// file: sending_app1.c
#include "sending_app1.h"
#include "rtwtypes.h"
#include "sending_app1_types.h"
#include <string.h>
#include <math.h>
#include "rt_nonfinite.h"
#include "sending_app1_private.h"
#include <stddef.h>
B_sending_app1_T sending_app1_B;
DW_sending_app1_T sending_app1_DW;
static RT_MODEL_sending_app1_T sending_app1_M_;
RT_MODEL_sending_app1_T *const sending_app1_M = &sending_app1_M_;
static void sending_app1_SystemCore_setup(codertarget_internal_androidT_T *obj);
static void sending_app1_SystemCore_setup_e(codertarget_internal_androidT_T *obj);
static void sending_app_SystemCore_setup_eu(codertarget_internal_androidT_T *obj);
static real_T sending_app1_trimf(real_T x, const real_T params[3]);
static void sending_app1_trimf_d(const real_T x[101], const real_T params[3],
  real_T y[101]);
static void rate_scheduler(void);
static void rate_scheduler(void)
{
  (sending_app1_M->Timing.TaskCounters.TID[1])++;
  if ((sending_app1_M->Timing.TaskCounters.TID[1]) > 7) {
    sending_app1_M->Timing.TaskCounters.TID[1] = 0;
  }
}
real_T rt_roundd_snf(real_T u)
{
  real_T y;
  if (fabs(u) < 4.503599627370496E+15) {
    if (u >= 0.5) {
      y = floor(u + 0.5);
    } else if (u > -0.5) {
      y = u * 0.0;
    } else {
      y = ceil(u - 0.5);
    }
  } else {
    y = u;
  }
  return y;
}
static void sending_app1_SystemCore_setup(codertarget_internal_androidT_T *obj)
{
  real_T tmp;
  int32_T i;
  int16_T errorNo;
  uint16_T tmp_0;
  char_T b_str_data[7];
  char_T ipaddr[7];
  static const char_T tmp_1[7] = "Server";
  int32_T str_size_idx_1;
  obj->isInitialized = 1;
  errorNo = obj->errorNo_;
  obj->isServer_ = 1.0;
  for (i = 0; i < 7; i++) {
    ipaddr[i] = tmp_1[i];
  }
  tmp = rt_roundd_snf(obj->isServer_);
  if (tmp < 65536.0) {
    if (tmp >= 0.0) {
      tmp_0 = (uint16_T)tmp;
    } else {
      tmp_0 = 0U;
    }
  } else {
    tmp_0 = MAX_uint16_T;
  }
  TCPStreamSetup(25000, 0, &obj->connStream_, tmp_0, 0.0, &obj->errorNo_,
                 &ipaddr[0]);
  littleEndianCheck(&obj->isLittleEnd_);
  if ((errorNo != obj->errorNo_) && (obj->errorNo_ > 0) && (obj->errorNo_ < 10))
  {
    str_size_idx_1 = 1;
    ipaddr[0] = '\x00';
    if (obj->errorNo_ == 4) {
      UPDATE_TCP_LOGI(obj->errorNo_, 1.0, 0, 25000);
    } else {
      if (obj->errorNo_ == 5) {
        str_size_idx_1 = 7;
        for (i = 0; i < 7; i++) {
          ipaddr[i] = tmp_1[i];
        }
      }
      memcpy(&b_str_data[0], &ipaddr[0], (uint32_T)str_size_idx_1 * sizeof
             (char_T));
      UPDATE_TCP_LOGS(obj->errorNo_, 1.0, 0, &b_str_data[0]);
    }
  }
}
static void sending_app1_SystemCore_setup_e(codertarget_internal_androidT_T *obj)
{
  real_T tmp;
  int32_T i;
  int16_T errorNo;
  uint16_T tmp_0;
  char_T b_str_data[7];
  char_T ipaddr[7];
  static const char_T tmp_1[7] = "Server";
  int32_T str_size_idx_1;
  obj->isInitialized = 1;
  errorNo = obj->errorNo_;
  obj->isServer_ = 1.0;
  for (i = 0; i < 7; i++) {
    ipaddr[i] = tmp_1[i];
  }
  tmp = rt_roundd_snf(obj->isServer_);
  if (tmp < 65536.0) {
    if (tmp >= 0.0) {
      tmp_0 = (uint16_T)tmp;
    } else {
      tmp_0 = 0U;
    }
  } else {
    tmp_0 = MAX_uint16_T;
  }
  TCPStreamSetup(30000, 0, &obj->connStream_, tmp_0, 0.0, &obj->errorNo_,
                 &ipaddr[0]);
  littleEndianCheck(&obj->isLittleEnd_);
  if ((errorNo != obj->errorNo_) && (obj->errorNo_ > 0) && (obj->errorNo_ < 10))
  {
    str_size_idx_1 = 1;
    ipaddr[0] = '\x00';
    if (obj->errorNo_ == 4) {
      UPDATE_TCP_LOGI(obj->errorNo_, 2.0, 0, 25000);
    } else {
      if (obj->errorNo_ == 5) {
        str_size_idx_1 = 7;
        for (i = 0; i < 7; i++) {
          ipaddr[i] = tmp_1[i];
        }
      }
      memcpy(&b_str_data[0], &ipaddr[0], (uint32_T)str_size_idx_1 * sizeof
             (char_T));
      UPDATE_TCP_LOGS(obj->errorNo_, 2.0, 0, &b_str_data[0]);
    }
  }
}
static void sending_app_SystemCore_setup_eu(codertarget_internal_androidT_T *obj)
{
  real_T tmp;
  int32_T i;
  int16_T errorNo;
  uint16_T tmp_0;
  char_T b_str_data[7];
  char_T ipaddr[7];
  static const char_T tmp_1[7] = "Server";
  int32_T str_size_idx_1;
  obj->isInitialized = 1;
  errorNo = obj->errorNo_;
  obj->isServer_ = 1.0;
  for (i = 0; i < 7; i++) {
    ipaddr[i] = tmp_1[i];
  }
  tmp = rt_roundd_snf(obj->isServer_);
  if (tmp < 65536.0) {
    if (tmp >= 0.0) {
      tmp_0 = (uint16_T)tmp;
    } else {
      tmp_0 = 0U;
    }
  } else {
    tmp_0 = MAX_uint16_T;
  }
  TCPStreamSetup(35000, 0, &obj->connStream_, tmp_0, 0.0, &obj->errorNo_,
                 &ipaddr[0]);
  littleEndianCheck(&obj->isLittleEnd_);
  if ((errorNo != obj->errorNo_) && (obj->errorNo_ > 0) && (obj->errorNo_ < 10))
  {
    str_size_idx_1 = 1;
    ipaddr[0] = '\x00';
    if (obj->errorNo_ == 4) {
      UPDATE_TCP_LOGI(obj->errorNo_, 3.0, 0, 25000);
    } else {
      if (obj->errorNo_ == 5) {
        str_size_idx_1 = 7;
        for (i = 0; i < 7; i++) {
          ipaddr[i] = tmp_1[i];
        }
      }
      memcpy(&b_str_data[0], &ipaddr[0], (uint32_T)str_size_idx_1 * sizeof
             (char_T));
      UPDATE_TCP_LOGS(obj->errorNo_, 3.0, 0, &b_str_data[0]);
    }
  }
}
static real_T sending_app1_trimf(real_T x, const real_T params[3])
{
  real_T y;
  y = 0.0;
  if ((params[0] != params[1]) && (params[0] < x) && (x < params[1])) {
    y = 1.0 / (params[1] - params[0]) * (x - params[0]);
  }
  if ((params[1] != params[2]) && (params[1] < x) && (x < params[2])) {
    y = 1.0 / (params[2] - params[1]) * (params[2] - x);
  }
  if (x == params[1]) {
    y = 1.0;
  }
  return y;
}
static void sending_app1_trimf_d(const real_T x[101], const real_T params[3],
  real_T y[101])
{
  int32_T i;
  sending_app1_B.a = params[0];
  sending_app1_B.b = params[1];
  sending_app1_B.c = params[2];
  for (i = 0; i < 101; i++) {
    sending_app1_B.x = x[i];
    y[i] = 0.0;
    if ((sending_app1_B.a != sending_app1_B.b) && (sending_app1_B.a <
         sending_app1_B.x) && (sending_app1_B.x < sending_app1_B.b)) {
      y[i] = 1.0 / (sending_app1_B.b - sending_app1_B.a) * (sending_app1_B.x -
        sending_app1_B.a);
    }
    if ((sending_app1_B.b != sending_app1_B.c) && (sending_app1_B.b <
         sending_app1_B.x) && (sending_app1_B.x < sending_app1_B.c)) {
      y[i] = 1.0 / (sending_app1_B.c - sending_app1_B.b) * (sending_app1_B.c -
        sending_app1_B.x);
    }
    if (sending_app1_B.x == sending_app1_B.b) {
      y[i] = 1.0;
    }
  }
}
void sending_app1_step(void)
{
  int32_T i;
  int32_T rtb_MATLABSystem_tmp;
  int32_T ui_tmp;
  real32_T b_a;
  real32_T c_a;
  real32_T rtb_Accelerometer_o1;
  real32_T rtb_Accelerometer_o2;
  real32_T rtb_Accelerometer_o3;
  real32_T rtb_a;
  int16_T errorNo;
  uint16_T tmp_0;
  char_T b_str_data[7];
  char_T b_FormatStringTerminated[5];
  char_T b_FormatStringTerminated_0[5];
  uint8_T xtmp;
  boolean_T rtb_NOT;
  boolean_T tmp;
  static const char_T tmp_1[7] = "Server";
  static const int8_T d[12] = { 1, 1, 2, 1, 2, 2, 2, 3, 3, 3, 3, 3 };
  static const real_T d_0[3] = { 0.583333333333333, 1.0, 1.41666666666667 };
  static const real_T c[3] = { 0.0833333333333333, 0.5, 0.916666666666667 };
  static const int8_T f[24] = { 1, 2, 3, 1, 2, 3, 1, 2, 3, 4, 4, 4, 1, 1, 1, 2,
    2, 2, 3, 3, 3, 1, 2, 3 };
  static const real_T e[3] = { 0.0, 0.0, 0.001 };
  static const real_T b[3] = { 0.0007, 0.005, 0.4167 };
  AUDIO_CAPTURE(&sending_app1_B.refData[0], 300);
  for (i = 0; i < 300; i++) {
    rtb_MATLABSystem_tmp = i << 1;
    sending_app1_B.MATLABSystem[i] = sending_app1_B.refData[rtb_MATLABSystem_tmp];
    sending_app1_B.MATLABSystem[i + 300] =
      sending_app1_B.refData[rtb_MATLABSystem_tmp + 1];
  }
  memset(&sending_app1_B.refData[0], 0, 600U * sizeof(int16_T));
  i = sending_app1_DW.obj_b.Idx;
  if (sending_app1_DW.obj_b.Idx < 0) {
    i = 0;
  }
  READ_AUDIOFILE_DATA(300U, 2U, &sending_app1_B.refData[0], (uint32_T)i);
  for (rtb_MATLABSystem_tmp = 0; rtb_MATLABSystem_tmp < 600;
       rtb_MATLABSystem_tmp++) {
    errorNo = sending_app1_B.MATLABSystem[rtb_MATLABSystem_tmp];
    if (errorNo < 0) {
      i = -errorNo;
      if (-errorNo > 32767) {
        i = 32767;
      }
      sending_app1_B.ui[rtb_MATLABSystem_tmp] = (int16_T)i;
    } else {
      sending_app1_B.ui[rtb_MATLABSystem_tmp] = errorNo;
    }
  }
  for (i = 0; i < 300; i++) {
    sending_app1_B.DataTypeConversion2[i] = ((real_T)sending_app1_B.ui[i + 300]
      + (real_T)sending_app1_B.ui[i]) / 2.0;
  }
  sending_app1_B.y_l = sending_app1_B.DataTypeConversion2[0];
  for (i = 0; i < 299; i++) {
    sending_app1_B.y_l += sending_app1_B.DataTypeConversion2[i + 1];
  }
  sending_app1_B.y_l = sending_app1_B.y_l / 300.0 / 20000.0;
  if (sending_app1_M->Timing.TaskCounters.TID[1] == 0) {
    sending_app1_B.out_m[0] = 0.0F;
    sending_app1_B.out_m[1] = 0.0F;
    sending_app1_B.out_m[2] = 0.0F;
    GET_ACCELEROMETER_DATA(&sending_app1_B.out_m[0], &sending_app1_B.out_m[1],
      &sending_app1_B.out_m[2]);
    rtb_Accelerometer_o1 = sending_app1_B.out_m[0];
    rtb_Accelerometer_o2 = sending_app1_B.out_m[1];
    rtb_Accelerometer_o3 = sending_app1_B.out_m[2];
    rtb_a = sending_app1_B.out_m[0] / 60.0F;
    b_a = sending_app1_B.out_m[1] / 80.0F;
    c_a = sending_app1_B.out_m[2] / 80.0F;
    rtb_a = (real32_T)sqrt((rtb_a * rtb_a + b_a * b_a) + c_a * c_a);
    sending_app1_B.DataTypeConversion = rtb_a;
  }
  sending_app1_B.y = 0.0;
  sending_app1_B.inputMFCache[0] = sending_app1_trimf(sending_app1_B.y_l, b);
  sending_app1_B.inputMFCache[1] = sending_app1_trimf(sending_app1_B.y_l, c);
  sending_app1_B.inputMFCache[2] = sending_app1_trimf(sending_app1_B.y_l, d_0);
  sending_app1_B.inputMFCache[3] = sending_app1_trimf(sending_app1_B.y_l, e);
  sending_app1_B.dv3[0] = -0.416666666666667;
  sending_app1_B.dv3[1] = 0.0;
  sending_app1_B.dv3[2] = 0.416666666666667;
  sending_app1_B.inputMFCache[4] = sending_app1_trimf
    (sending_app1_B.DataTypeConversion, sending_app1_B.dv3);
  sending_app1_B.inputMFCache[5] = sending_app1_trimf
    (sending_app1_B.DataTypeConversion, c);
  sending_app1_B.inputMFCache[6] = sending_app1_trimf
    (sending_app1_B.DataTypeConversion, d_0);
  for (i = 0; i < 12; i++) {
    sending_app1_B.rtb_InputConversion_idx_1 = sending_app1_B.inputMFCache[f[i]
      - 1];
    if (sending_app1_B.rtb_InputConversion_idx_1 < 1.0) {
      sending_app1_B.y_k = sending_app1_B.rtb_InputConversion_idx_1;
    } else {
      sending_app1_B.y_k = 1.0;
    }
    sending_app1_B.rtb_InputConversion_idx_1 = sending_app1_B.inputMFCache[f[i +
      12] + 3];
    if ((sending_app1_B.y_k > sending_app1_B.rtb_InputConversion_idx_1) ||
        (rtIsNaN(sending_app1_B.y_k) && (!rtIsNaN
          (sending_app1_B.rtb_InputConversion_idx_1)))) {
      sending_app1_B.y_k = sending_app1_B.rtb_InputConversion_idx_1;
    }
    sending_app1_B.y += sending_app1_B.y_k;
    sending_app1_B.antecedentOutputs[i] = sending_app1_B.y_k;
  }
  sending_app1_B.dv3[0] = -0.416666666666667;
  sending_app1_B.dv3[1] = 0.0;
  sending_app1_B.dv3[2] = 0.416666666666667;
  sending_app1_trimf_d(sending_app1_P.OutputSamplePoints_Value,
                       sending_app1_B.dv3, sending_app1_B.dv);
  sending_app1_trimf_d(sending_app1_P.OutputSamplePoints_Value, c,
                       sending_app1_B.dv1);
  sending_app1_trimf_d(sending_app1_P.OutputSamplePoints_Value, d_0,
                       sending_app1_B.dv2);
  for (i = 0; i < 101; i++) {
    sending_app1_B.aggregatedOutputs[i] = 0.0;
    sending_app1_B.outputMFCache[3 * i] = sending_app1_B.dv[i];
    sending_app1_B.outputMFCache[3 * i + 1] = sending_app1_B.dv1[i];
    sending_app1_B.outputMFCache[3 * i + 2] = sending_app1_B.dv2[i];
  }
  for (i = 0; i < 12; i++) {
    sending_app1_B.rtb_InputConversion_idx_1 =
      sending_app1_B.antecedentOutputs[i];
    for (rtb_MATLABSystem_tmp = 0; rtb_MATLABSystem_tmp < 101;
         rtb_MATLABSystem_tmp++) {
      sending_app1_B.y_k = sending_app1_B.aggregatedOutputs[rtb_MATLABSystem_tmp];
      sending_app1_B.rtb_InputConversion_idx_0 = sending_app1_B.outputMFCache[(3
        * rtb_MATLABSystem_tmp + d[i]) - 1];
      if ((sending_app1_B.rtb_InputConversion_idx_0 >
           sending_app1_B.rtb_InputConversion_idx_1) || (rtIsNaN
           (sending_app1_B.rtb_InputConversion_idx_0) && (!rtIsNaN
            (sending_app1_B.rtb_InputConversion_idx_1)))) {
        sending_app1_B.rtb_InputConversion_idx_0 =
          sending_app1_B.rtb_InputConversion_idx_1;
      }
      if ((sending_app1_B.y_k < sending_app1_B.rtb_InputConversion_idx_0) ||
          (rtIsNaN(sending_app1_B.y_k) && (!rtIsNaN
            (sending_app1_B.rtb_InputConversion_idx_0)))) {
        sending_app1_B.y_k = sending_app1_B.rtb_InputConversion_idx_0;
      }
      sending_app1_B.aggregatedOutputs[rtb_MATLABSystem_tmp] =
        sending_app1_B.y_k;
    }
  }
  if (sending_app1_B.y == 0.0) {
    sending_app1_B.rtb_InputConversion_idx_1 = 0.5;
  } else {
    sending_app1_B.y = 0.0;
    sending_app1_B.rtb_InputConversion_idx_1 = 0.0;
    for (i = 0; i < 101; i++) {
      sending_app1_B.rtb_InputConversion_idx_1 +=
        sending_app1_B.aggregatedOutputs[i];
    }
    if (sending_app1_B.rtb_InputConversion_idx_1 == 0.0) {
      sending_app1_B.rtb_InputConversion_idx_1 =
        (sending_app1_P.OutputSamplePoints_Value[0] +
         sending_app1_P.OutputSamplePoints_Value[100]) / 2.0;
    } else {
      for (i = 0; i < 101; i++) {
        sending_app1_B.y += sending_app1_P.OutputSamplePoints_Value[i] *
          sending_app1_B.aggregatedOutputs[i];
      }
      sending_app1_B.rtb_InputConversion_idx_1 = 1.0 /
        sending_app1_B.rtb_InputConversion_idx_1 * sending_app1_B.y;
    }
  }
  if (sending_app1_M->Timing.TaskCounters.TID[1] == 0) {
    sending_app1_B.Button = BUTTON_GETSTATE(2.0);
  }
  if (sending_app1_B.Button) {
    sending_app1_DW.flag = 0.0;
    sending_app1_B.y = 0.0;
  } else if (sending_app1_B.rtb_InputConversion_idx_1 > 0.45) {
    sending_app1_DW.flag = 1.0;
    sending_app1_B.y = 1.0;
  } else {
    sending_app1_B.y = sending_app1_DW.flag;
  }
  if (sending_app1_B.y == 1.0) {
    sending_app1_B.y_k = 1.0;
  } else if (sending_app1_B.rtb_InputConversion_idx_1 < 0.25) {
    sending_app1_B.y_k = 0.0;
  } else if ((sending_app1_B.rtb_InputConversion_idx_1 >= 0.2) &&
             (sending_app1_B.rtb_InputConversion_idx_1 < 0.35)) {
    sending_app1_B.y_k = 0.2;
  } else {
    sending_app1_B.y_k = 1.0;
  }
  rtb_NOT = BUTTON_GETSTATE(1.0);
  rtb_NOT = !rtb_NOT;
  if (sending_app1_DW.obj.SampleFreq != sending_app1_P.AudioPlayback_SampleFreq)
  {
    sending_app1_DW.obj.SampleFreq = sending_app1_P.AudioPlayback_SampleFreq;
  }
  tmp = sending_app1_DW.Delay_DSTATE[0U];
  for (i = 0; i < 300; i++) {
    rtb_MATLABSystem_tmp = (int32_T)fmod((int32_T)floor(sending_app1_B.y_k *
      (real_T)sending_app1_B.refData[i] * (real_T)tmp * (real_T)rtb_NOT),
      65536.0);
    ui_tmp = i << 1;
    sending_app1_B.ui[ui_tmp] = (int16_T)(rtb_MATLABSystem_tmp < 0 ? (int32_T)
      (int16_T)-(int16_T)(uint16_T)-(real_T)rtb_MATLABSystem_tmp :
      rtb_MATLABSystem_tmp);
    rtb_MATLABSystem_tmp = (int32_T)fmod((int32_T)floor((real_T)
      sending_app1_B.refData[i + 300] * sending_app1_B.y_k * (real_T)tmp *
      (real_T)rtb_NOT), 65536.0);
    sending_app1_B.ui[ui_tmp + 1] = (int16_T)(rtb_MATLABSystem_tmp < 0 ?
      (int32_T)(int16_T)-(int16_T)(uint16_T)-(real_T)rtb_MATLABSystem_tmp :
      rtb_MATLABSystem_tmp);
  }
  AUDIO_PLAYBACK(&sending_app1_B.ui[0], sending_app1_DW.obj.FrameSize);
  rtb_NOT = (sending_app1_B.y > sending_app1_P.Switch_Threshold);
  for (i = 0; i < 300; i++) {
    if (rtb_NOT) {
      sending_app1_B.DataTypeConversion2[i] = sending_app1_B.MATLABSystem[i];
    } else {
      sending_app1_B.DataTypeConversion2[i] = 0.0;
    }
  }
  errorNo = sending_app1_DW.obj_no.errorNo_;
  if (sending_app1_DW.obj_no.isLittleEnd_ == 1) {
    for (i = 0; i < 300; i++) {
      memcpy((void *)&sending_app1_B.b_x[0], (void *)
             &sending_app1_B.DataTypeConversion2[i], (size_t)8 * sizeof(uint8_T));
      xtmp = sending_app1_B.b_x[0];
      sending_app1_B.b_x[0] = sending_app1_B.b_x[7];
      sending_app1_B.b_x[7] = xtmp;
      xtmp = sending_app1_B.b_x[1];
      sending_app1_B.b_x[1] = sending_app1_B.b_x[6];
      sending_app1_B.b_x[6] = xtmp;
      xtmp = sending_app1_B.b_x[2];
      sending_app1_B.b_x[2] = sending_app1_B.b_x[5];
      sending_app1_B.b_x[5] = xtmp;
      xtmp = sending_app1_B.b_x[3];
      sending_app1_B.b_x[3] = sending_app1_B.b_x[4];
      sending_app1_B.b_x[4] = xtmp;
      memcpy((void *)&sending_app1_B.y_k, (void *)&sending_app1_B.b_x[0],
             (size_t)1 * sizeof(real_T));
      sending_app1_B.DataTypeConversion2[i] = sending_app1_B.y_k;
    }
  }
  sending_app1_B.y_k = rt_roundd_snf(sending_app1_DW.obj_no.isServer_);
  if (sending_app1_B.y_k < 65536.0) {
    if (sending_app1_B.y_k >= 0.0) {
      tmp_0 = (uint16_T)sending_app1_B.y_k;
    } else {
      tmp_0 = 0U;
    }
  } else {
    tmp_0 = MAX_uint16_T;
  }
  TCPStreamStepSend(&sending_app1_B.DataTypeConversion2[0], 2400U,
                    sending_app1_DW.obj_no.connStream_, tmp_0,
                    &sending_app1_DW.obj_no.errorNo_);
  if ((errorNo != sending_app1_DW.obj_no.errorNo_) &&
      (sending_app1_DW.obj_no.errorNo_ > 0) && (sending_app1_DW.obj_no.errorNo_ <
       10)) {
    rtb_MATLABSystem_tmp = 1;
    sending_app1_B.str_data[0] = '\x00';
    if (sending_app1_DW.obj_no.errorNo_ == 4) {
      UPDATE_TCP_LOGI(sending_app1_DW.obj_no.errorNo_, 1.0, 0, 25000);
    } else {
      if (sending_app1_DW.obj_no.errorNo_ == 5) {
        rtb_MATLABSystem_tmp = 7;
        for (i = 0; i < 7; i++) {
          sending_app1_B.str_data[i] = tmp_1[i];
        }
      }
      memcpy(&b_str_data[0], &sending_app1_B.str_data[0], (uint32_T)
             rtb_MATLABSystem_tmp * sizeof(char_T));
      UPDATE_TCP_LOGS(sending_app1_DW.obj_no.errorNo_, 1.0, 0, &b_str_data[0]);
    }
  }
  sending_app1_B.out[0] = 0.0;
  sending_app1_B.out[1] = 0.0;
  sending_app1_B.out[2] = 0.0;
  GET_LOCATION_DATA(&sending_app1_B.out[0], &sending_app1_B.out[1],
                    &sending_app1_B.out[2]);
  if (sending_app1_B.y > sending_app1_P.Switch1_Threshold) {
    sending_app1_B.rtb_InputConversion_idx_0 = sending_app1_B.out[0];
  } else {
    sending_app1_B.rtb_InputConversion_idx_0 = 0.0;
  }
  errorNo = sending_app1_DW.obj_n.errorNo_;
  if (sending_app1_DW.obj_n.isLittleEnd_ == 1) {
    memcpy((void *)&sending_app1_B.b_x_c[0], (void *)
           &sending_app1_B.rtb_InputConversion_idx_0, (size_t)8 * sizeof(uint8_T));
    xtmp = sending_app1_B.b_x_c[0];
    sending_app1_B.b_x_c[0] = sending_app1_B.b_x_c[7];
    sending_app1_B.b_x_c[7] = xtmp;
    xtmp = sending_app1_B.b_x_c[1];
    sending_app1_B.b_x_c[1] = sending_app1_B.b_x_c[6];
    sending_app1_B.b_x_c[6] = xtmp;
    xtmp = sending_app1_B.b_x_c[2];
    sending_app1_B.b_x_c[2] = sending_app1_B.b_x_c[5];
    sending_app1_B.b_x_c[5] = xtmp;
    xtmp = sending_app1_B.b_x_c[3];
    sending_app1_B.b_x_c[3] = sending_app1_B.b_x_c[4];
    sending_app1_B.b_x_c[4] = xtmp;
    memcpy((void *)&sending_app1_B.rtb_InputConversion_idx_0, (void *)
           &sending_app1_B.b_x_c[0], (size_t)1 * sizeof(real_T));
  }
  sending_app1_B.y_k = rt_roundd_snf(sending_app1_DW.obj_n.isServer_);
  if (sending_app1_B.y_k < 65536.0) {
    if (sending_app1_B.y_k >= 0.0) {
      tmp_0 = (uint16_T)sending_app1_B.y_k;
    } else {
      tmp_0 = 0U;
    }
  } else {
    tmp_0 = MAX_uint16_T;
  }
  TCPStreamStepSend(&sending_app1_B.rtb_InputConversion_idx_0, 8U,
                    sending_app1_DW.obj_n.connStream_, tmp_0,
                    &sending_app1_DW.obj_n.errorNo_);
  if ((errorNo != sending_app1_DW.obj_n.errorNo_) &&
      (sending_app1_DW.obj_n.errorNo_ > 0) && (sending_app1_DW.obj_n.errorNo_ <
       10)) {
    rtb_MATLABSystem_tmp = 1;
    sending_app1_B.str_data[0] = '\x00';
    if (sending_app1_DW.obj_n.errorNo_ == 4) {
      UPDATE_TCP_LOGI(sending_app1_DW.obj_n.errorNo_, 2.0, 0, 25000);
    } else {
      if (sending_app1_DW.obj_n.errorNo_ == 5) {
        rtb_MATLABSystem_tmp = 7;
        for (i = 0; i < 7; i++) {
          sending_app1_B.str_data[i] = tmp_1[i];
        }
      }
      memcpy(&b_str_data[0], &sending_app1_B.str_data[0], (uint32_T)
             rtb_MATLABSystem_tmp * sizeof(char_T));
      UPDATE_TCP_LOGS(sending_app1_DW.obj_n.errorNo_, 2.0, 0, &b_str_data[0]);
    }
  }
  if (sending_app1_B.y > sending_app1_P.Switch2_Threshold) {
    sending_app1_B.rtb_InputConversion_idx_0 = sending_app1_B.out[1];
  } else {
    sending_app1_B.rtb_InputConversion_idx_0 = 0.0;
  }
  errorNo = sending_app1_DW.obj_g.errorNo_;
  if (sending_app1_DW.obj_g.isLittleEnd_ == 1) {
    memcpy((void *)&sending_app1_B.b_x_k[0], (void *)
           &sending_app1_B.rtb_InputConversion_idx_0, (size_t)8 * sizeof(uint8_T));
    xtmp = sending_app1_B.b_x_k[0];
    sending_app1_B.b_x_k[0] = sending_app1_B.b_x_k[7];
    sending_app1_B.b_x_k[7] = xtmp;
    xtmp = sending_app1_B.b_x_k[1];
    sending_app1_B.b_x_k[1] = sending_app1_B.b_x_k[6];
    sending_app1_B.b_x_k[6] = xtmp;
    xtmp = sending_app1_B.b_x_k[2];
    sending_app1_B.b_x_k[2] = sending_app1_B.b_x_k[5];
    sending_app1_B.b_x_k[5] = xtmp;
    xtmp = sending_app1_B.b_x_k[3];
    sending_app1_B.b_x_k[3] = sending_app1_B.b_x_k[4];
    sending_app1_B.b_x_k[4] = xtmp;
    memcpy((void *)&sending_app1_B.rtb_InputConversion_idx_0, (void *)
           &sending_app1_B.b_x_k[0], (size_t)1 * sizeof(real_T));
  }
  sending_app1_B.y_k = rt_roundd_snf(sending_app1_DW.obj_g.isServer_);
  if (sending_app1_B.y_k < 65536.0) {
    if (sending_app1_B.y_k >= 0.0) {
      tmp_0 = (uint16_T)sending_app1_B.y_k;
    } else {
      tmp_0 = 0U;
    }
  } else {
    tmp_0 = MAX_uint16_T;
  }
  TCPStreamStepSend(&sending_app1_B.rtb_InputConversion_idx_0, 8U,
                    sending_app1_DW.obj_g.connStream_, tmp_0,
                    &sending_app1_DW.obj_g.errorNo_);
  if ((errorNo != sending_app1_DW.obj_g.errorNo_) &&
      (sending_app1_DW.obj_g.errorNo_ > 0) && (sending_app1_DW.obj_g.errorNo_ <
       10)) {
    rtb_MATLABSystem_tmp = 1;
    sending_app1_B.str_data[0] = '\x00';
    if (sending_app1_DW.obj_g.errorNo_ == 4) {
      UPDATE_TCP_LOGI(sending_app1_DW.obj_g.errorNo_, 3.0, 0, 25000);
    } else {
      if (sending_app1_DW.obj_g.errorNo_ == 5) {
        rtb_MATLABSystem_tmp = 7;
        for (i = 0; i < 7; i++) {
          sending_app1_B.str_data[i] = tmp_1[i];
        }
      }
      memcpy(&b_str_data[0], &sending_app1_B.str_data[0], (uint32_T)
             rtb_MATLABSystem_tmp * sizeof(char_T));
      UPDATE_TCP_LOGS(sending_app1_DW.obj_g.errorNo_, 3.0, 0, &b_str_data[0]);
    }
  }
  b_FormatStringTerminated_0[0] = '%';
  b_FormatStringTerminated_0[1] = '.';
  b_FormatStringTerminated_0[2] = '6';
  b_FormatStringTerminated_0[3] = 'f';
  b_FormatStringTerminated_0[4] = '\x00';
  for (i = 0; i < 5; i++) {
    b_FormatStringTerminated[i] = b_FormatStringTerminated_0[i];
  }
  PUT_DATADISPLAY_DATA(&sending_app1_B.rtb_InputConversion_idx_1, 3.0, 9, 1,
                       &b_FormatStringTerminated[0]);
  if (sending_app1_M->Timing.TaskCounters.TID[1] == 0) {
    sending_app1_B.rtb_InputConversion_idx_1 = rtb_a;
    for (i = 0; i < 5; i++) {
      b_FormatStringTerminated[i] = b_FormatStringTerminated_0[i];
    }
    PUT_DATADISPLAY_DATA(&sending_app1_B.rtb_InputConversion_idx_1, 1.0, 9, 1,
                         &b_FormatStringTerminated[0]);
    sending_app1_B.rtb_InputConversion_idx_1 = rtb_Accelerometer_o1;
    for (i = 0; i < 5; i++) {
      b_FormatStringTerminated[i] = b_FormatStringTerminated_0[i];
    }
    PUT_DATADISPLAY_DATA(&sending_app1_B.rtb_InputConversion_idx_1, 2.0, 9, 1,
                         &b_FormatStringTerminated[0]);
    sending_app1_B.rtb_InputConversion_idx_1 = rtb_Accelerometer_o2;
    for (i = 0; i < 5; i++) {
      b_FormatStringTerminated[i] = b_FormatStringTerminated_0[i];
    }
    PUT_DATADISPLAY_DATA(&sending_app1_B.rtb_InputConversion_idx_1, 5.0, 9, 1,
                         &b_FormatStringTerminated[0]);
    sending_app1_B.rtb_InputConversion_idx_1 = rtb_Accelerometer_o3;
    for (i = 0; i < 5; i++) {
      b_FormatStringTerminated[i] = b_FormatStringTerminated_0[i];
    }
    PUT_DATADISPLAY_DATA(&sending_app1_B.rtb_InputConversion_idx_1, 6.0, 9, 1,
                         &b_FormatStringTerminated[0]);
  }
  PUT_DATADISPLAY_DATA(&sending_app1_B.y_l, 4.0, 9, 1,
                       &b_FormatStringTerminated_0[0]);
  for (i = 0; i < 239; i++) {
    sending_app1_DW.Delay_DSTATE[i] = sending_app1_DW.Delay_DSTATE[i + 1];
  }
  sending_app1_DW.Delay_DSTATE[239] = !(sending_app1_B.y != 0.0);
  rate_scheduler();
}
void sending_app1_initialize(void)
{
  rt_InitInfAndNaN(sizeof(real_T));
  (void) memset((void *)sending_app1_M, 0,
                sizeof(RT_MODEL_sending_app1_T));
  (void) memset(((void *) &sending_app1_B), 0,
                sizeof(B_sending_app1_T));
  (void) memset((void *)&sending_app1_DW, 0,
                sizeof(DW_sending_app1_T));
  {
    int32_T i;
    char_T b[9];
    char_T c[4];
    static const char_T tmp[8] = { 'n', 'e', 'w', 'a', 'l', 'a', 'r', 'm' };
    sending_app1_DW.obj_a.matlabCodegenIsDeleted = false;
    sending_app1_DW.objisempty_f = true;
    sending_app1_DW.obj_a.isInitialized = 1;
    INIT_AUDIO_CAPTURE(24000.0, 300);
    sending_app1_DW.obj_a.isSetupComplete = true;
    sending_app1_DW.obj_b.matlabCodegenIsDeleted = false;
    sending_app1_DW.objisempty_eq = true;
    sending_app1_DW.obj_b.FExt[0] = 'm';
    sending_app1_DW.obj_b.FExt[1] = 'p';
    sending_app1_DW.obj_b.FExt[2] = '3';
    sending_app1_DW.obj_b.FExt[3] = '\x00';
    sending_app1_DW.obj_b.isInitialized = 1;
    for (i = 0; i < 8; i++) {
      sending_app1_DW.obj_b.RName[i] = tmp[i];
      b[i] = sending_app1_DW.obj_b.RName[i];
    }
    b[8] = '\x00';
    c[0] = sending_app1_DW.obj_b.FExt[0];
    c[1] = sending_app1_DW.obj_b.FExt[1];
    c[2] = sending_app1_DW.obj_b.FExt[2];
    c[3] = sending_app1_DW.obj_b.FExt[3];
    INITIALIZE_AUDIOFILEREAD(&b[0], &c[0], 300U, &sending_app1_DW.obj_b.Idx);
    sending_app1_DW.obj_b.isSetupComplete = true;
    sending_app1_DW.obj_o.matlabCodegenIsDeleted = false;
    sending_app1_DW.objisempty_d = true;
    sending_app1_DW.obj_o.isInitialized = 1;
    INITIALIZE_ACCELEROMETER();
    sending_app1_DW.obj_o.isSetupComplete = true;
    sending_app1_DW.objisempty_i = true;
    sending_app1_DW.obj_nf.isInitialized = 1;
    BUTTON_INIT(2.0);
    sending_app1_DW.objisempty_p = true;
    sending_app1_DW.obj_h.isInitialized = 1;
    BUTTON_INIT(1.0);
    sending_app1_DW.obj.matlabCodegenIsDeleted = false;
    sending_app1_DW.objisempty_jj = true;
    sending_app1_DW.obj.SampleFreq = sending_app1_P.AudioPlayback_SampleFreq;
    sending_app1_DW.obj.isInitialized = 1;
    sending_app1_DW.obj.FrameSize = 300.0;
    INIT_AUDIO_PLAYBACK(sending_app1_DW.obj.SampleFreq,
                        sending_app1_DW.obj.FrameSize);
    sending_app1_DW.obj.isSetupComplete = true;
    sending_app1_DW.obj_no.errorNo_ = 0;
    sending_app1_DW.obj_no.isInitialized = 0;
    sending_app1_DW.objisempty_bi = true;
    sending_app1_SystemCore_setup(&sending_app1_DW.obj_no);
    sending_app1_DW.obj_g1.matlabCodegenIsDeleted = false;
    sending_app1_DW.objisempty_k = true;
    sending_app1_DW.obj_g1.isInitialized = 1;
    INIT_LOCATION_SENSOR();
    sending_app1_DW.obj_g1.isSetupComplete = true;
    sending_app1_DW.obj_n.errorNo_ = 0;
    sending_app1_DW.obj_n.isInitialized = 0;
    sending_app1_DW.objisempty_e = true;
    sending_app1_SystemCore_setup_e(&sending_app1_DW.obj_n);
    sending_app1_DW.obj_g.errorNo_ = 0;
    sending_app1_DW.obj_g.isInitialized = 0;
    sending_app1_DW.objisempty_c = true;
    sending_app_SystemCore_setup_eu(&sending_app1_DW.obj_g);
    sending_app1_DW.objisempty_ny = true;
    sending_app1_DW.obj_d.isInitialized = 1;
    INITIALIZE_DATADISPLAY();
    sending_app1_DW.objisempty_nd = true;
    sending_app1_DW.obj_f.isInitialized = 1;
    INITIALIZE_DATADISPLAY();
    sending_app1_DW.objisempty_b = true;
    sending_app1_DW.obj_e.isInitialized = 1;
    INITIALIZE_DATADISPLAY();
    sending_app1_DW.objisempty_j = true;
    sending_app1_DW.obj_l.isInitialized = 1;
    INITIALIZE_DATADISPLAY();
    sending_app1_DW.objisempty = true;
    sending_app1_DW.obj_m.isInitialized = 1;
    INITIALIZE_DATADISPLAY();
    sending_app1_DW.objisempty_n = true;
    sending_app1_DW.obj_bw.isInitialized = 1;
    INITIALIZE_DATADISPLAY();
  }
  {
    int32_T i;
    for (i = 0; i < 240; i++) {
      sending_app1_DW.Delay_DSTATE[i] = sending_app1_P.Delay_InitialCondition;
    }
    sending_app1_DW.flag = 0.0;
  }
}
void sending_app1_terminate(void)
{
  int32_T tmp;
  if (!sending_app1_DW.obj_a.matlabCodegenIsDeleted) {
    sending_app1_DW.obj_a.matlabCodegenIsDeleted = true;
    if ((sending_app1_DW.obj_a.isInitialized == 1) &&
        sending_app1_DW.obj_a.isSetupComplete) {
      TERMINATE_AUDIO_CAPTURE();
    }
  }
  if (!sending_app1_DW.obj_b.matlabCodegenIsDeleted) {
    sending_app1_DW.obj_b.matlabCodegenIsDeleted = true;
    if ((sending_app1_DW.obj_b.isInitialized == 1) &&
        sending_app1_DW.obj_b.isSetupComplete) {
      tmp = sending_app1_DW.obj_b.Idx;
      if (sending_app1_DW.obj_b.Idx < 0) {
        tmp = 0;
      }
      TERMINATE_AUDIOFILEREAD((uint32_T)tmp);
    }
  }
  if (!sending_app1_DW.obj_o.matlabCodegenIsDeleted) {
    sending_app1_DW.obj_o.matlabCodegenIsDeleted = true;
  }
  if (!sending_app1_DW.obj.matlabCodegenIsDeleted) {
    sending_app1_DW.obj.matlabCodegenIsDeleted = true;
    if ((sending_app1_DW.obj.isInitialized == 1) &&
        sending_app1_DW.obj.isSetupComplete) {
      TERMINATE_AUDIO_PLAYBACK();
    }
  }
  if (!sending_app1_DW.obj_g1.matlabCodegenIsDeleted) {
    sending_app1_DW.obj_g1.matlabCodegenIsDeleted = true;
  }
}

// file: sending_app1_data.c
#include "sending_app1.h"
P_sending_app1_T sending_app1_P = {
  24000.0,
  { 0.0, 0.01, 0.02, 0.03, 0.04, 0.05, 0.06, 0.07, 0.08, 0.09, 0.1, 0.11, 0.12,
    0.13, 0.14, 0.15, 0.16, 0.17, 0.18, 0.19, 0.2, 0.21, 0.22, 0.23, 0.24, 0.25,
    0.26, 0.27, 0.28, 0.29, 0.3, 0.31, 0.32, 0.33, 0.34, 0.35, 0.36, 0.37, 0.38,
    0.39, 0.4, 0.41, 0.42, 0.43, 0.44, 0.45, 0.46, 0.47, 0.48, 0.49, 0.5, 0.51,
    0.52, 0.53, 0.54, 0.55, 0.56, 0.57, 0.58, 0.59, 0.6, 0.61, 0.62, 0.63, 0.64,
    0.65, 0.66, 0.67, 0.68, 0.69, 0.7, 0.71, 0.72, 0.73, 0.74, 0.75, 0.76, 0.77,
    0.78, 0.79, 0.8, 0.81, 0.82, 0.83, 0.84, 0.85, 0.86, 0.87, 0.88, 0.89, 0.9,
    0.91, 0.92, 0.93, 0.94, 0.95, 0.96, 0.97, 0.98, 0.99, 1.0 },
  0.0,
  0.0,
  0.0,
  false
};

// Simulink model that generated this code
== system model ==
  DataDisplay#1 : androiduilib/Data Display  <- 1: MATLABFunction#1
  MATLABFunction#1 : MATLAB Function  <- 1: AudioCapture#1
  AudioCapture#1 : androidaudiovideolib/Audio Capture
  DataDisplay#2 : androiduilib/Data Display  <- 1: Accelerometer
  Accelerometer : androidsensorlib/Accelerometer
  DataDisplay#3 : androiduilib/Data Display  <- 1: Accelerometer/2
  DataDisplay#4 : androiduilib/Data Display  <- 1: Accelerometer/3
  DataDisplay#5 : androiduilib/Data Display  <- 1: MATLABFunction#2
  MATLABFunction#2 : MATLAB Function  <- 1: Accelerometer, 2: Accelerometer/2, 3: Accelerometer/3
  DataTypeConversion : DataTypeConversion  <- 1: MATLABFunction#2
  AudioPlayback : androidaudiovideolib/Audio Playback  <- 1: DataTypeConversion#1
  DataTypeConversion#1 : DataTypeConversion  <- 1: Product#1
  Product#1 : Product  Inputs=4  <- 1: MATLABFunction#3, 2: AudioFileRead#1, 3: Delay, 4: NOT
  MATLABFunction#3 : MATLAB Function  <- 2: MATLABFunction#4
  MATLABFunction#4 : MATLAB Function  <- 1: Button#1
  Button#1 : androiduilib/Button
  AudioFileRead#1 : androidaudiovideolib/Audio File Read
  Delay : Delay  DelayLength=240  <- 1: Logic#1
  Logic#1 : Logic  Operator=NOT  <- 1: MATLABFunction#4
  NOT : Logic  Operator=NOT  <- 1: Button#2
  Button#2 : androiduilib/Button
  IPSend#1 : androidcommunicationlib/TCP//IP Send  <- 1: DataTypeConversion2
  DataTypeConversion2 : DataTypeConversion  <- 1: Switch
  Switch : Switch  Criteria=u2 > Threshold  <- 1: MATLABFunction#5, 2: MATLABFunction#4
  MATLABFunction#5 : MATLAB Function  <- 1: AudioCapture#1
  IPSend#2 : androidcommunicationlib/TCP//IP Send  <- 1: DataTypeConversion#2
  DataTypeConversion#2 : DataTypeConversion  <- 1: Switch1
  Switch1 : Switch  Criteria=u2 > Threshold  <- 1: LocationSensor#1, 2: MATLABFunction#4
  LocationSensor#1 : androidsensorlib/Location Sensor
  IPSend#3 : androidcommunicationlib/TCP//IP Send  <- 1: DataTypeConversion#3
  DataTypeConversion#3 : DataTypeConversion  <- 1: Switch2
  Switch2 : Switch  Criteria=u2 > Threshold  <- 1: LocationSensor#1/2, 2: MATLABFunction#4
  DataDisplay#6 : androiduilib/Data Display
== matlab function MATLABFunction#2 ==
function a = fcn(x,y,z)
x = x/60;
y = y/80;
z = z/80;

ai = (x^2)+(y^2)+(z^2);
b = ai^0.5;
a = b;

== matlab function MATLABFunction#5 ==
function y = fcn(u)
y = u(:,1);

== matlab function MATLABFunction#3 ==
function y = fcn(u, v)
    if v ==1
               y = 1;
    elseif u < 0.25
        y = 0;
    elseif u >= 0.20 && u < 0.35
        y = 0.2;
    else
        y = 1;
    end

== matlab function MATLABFunction#1 ==
function y = fcn(u)
ui = abs(u);
yi = mean(ui,2);
y = mean(yi)/20000;
